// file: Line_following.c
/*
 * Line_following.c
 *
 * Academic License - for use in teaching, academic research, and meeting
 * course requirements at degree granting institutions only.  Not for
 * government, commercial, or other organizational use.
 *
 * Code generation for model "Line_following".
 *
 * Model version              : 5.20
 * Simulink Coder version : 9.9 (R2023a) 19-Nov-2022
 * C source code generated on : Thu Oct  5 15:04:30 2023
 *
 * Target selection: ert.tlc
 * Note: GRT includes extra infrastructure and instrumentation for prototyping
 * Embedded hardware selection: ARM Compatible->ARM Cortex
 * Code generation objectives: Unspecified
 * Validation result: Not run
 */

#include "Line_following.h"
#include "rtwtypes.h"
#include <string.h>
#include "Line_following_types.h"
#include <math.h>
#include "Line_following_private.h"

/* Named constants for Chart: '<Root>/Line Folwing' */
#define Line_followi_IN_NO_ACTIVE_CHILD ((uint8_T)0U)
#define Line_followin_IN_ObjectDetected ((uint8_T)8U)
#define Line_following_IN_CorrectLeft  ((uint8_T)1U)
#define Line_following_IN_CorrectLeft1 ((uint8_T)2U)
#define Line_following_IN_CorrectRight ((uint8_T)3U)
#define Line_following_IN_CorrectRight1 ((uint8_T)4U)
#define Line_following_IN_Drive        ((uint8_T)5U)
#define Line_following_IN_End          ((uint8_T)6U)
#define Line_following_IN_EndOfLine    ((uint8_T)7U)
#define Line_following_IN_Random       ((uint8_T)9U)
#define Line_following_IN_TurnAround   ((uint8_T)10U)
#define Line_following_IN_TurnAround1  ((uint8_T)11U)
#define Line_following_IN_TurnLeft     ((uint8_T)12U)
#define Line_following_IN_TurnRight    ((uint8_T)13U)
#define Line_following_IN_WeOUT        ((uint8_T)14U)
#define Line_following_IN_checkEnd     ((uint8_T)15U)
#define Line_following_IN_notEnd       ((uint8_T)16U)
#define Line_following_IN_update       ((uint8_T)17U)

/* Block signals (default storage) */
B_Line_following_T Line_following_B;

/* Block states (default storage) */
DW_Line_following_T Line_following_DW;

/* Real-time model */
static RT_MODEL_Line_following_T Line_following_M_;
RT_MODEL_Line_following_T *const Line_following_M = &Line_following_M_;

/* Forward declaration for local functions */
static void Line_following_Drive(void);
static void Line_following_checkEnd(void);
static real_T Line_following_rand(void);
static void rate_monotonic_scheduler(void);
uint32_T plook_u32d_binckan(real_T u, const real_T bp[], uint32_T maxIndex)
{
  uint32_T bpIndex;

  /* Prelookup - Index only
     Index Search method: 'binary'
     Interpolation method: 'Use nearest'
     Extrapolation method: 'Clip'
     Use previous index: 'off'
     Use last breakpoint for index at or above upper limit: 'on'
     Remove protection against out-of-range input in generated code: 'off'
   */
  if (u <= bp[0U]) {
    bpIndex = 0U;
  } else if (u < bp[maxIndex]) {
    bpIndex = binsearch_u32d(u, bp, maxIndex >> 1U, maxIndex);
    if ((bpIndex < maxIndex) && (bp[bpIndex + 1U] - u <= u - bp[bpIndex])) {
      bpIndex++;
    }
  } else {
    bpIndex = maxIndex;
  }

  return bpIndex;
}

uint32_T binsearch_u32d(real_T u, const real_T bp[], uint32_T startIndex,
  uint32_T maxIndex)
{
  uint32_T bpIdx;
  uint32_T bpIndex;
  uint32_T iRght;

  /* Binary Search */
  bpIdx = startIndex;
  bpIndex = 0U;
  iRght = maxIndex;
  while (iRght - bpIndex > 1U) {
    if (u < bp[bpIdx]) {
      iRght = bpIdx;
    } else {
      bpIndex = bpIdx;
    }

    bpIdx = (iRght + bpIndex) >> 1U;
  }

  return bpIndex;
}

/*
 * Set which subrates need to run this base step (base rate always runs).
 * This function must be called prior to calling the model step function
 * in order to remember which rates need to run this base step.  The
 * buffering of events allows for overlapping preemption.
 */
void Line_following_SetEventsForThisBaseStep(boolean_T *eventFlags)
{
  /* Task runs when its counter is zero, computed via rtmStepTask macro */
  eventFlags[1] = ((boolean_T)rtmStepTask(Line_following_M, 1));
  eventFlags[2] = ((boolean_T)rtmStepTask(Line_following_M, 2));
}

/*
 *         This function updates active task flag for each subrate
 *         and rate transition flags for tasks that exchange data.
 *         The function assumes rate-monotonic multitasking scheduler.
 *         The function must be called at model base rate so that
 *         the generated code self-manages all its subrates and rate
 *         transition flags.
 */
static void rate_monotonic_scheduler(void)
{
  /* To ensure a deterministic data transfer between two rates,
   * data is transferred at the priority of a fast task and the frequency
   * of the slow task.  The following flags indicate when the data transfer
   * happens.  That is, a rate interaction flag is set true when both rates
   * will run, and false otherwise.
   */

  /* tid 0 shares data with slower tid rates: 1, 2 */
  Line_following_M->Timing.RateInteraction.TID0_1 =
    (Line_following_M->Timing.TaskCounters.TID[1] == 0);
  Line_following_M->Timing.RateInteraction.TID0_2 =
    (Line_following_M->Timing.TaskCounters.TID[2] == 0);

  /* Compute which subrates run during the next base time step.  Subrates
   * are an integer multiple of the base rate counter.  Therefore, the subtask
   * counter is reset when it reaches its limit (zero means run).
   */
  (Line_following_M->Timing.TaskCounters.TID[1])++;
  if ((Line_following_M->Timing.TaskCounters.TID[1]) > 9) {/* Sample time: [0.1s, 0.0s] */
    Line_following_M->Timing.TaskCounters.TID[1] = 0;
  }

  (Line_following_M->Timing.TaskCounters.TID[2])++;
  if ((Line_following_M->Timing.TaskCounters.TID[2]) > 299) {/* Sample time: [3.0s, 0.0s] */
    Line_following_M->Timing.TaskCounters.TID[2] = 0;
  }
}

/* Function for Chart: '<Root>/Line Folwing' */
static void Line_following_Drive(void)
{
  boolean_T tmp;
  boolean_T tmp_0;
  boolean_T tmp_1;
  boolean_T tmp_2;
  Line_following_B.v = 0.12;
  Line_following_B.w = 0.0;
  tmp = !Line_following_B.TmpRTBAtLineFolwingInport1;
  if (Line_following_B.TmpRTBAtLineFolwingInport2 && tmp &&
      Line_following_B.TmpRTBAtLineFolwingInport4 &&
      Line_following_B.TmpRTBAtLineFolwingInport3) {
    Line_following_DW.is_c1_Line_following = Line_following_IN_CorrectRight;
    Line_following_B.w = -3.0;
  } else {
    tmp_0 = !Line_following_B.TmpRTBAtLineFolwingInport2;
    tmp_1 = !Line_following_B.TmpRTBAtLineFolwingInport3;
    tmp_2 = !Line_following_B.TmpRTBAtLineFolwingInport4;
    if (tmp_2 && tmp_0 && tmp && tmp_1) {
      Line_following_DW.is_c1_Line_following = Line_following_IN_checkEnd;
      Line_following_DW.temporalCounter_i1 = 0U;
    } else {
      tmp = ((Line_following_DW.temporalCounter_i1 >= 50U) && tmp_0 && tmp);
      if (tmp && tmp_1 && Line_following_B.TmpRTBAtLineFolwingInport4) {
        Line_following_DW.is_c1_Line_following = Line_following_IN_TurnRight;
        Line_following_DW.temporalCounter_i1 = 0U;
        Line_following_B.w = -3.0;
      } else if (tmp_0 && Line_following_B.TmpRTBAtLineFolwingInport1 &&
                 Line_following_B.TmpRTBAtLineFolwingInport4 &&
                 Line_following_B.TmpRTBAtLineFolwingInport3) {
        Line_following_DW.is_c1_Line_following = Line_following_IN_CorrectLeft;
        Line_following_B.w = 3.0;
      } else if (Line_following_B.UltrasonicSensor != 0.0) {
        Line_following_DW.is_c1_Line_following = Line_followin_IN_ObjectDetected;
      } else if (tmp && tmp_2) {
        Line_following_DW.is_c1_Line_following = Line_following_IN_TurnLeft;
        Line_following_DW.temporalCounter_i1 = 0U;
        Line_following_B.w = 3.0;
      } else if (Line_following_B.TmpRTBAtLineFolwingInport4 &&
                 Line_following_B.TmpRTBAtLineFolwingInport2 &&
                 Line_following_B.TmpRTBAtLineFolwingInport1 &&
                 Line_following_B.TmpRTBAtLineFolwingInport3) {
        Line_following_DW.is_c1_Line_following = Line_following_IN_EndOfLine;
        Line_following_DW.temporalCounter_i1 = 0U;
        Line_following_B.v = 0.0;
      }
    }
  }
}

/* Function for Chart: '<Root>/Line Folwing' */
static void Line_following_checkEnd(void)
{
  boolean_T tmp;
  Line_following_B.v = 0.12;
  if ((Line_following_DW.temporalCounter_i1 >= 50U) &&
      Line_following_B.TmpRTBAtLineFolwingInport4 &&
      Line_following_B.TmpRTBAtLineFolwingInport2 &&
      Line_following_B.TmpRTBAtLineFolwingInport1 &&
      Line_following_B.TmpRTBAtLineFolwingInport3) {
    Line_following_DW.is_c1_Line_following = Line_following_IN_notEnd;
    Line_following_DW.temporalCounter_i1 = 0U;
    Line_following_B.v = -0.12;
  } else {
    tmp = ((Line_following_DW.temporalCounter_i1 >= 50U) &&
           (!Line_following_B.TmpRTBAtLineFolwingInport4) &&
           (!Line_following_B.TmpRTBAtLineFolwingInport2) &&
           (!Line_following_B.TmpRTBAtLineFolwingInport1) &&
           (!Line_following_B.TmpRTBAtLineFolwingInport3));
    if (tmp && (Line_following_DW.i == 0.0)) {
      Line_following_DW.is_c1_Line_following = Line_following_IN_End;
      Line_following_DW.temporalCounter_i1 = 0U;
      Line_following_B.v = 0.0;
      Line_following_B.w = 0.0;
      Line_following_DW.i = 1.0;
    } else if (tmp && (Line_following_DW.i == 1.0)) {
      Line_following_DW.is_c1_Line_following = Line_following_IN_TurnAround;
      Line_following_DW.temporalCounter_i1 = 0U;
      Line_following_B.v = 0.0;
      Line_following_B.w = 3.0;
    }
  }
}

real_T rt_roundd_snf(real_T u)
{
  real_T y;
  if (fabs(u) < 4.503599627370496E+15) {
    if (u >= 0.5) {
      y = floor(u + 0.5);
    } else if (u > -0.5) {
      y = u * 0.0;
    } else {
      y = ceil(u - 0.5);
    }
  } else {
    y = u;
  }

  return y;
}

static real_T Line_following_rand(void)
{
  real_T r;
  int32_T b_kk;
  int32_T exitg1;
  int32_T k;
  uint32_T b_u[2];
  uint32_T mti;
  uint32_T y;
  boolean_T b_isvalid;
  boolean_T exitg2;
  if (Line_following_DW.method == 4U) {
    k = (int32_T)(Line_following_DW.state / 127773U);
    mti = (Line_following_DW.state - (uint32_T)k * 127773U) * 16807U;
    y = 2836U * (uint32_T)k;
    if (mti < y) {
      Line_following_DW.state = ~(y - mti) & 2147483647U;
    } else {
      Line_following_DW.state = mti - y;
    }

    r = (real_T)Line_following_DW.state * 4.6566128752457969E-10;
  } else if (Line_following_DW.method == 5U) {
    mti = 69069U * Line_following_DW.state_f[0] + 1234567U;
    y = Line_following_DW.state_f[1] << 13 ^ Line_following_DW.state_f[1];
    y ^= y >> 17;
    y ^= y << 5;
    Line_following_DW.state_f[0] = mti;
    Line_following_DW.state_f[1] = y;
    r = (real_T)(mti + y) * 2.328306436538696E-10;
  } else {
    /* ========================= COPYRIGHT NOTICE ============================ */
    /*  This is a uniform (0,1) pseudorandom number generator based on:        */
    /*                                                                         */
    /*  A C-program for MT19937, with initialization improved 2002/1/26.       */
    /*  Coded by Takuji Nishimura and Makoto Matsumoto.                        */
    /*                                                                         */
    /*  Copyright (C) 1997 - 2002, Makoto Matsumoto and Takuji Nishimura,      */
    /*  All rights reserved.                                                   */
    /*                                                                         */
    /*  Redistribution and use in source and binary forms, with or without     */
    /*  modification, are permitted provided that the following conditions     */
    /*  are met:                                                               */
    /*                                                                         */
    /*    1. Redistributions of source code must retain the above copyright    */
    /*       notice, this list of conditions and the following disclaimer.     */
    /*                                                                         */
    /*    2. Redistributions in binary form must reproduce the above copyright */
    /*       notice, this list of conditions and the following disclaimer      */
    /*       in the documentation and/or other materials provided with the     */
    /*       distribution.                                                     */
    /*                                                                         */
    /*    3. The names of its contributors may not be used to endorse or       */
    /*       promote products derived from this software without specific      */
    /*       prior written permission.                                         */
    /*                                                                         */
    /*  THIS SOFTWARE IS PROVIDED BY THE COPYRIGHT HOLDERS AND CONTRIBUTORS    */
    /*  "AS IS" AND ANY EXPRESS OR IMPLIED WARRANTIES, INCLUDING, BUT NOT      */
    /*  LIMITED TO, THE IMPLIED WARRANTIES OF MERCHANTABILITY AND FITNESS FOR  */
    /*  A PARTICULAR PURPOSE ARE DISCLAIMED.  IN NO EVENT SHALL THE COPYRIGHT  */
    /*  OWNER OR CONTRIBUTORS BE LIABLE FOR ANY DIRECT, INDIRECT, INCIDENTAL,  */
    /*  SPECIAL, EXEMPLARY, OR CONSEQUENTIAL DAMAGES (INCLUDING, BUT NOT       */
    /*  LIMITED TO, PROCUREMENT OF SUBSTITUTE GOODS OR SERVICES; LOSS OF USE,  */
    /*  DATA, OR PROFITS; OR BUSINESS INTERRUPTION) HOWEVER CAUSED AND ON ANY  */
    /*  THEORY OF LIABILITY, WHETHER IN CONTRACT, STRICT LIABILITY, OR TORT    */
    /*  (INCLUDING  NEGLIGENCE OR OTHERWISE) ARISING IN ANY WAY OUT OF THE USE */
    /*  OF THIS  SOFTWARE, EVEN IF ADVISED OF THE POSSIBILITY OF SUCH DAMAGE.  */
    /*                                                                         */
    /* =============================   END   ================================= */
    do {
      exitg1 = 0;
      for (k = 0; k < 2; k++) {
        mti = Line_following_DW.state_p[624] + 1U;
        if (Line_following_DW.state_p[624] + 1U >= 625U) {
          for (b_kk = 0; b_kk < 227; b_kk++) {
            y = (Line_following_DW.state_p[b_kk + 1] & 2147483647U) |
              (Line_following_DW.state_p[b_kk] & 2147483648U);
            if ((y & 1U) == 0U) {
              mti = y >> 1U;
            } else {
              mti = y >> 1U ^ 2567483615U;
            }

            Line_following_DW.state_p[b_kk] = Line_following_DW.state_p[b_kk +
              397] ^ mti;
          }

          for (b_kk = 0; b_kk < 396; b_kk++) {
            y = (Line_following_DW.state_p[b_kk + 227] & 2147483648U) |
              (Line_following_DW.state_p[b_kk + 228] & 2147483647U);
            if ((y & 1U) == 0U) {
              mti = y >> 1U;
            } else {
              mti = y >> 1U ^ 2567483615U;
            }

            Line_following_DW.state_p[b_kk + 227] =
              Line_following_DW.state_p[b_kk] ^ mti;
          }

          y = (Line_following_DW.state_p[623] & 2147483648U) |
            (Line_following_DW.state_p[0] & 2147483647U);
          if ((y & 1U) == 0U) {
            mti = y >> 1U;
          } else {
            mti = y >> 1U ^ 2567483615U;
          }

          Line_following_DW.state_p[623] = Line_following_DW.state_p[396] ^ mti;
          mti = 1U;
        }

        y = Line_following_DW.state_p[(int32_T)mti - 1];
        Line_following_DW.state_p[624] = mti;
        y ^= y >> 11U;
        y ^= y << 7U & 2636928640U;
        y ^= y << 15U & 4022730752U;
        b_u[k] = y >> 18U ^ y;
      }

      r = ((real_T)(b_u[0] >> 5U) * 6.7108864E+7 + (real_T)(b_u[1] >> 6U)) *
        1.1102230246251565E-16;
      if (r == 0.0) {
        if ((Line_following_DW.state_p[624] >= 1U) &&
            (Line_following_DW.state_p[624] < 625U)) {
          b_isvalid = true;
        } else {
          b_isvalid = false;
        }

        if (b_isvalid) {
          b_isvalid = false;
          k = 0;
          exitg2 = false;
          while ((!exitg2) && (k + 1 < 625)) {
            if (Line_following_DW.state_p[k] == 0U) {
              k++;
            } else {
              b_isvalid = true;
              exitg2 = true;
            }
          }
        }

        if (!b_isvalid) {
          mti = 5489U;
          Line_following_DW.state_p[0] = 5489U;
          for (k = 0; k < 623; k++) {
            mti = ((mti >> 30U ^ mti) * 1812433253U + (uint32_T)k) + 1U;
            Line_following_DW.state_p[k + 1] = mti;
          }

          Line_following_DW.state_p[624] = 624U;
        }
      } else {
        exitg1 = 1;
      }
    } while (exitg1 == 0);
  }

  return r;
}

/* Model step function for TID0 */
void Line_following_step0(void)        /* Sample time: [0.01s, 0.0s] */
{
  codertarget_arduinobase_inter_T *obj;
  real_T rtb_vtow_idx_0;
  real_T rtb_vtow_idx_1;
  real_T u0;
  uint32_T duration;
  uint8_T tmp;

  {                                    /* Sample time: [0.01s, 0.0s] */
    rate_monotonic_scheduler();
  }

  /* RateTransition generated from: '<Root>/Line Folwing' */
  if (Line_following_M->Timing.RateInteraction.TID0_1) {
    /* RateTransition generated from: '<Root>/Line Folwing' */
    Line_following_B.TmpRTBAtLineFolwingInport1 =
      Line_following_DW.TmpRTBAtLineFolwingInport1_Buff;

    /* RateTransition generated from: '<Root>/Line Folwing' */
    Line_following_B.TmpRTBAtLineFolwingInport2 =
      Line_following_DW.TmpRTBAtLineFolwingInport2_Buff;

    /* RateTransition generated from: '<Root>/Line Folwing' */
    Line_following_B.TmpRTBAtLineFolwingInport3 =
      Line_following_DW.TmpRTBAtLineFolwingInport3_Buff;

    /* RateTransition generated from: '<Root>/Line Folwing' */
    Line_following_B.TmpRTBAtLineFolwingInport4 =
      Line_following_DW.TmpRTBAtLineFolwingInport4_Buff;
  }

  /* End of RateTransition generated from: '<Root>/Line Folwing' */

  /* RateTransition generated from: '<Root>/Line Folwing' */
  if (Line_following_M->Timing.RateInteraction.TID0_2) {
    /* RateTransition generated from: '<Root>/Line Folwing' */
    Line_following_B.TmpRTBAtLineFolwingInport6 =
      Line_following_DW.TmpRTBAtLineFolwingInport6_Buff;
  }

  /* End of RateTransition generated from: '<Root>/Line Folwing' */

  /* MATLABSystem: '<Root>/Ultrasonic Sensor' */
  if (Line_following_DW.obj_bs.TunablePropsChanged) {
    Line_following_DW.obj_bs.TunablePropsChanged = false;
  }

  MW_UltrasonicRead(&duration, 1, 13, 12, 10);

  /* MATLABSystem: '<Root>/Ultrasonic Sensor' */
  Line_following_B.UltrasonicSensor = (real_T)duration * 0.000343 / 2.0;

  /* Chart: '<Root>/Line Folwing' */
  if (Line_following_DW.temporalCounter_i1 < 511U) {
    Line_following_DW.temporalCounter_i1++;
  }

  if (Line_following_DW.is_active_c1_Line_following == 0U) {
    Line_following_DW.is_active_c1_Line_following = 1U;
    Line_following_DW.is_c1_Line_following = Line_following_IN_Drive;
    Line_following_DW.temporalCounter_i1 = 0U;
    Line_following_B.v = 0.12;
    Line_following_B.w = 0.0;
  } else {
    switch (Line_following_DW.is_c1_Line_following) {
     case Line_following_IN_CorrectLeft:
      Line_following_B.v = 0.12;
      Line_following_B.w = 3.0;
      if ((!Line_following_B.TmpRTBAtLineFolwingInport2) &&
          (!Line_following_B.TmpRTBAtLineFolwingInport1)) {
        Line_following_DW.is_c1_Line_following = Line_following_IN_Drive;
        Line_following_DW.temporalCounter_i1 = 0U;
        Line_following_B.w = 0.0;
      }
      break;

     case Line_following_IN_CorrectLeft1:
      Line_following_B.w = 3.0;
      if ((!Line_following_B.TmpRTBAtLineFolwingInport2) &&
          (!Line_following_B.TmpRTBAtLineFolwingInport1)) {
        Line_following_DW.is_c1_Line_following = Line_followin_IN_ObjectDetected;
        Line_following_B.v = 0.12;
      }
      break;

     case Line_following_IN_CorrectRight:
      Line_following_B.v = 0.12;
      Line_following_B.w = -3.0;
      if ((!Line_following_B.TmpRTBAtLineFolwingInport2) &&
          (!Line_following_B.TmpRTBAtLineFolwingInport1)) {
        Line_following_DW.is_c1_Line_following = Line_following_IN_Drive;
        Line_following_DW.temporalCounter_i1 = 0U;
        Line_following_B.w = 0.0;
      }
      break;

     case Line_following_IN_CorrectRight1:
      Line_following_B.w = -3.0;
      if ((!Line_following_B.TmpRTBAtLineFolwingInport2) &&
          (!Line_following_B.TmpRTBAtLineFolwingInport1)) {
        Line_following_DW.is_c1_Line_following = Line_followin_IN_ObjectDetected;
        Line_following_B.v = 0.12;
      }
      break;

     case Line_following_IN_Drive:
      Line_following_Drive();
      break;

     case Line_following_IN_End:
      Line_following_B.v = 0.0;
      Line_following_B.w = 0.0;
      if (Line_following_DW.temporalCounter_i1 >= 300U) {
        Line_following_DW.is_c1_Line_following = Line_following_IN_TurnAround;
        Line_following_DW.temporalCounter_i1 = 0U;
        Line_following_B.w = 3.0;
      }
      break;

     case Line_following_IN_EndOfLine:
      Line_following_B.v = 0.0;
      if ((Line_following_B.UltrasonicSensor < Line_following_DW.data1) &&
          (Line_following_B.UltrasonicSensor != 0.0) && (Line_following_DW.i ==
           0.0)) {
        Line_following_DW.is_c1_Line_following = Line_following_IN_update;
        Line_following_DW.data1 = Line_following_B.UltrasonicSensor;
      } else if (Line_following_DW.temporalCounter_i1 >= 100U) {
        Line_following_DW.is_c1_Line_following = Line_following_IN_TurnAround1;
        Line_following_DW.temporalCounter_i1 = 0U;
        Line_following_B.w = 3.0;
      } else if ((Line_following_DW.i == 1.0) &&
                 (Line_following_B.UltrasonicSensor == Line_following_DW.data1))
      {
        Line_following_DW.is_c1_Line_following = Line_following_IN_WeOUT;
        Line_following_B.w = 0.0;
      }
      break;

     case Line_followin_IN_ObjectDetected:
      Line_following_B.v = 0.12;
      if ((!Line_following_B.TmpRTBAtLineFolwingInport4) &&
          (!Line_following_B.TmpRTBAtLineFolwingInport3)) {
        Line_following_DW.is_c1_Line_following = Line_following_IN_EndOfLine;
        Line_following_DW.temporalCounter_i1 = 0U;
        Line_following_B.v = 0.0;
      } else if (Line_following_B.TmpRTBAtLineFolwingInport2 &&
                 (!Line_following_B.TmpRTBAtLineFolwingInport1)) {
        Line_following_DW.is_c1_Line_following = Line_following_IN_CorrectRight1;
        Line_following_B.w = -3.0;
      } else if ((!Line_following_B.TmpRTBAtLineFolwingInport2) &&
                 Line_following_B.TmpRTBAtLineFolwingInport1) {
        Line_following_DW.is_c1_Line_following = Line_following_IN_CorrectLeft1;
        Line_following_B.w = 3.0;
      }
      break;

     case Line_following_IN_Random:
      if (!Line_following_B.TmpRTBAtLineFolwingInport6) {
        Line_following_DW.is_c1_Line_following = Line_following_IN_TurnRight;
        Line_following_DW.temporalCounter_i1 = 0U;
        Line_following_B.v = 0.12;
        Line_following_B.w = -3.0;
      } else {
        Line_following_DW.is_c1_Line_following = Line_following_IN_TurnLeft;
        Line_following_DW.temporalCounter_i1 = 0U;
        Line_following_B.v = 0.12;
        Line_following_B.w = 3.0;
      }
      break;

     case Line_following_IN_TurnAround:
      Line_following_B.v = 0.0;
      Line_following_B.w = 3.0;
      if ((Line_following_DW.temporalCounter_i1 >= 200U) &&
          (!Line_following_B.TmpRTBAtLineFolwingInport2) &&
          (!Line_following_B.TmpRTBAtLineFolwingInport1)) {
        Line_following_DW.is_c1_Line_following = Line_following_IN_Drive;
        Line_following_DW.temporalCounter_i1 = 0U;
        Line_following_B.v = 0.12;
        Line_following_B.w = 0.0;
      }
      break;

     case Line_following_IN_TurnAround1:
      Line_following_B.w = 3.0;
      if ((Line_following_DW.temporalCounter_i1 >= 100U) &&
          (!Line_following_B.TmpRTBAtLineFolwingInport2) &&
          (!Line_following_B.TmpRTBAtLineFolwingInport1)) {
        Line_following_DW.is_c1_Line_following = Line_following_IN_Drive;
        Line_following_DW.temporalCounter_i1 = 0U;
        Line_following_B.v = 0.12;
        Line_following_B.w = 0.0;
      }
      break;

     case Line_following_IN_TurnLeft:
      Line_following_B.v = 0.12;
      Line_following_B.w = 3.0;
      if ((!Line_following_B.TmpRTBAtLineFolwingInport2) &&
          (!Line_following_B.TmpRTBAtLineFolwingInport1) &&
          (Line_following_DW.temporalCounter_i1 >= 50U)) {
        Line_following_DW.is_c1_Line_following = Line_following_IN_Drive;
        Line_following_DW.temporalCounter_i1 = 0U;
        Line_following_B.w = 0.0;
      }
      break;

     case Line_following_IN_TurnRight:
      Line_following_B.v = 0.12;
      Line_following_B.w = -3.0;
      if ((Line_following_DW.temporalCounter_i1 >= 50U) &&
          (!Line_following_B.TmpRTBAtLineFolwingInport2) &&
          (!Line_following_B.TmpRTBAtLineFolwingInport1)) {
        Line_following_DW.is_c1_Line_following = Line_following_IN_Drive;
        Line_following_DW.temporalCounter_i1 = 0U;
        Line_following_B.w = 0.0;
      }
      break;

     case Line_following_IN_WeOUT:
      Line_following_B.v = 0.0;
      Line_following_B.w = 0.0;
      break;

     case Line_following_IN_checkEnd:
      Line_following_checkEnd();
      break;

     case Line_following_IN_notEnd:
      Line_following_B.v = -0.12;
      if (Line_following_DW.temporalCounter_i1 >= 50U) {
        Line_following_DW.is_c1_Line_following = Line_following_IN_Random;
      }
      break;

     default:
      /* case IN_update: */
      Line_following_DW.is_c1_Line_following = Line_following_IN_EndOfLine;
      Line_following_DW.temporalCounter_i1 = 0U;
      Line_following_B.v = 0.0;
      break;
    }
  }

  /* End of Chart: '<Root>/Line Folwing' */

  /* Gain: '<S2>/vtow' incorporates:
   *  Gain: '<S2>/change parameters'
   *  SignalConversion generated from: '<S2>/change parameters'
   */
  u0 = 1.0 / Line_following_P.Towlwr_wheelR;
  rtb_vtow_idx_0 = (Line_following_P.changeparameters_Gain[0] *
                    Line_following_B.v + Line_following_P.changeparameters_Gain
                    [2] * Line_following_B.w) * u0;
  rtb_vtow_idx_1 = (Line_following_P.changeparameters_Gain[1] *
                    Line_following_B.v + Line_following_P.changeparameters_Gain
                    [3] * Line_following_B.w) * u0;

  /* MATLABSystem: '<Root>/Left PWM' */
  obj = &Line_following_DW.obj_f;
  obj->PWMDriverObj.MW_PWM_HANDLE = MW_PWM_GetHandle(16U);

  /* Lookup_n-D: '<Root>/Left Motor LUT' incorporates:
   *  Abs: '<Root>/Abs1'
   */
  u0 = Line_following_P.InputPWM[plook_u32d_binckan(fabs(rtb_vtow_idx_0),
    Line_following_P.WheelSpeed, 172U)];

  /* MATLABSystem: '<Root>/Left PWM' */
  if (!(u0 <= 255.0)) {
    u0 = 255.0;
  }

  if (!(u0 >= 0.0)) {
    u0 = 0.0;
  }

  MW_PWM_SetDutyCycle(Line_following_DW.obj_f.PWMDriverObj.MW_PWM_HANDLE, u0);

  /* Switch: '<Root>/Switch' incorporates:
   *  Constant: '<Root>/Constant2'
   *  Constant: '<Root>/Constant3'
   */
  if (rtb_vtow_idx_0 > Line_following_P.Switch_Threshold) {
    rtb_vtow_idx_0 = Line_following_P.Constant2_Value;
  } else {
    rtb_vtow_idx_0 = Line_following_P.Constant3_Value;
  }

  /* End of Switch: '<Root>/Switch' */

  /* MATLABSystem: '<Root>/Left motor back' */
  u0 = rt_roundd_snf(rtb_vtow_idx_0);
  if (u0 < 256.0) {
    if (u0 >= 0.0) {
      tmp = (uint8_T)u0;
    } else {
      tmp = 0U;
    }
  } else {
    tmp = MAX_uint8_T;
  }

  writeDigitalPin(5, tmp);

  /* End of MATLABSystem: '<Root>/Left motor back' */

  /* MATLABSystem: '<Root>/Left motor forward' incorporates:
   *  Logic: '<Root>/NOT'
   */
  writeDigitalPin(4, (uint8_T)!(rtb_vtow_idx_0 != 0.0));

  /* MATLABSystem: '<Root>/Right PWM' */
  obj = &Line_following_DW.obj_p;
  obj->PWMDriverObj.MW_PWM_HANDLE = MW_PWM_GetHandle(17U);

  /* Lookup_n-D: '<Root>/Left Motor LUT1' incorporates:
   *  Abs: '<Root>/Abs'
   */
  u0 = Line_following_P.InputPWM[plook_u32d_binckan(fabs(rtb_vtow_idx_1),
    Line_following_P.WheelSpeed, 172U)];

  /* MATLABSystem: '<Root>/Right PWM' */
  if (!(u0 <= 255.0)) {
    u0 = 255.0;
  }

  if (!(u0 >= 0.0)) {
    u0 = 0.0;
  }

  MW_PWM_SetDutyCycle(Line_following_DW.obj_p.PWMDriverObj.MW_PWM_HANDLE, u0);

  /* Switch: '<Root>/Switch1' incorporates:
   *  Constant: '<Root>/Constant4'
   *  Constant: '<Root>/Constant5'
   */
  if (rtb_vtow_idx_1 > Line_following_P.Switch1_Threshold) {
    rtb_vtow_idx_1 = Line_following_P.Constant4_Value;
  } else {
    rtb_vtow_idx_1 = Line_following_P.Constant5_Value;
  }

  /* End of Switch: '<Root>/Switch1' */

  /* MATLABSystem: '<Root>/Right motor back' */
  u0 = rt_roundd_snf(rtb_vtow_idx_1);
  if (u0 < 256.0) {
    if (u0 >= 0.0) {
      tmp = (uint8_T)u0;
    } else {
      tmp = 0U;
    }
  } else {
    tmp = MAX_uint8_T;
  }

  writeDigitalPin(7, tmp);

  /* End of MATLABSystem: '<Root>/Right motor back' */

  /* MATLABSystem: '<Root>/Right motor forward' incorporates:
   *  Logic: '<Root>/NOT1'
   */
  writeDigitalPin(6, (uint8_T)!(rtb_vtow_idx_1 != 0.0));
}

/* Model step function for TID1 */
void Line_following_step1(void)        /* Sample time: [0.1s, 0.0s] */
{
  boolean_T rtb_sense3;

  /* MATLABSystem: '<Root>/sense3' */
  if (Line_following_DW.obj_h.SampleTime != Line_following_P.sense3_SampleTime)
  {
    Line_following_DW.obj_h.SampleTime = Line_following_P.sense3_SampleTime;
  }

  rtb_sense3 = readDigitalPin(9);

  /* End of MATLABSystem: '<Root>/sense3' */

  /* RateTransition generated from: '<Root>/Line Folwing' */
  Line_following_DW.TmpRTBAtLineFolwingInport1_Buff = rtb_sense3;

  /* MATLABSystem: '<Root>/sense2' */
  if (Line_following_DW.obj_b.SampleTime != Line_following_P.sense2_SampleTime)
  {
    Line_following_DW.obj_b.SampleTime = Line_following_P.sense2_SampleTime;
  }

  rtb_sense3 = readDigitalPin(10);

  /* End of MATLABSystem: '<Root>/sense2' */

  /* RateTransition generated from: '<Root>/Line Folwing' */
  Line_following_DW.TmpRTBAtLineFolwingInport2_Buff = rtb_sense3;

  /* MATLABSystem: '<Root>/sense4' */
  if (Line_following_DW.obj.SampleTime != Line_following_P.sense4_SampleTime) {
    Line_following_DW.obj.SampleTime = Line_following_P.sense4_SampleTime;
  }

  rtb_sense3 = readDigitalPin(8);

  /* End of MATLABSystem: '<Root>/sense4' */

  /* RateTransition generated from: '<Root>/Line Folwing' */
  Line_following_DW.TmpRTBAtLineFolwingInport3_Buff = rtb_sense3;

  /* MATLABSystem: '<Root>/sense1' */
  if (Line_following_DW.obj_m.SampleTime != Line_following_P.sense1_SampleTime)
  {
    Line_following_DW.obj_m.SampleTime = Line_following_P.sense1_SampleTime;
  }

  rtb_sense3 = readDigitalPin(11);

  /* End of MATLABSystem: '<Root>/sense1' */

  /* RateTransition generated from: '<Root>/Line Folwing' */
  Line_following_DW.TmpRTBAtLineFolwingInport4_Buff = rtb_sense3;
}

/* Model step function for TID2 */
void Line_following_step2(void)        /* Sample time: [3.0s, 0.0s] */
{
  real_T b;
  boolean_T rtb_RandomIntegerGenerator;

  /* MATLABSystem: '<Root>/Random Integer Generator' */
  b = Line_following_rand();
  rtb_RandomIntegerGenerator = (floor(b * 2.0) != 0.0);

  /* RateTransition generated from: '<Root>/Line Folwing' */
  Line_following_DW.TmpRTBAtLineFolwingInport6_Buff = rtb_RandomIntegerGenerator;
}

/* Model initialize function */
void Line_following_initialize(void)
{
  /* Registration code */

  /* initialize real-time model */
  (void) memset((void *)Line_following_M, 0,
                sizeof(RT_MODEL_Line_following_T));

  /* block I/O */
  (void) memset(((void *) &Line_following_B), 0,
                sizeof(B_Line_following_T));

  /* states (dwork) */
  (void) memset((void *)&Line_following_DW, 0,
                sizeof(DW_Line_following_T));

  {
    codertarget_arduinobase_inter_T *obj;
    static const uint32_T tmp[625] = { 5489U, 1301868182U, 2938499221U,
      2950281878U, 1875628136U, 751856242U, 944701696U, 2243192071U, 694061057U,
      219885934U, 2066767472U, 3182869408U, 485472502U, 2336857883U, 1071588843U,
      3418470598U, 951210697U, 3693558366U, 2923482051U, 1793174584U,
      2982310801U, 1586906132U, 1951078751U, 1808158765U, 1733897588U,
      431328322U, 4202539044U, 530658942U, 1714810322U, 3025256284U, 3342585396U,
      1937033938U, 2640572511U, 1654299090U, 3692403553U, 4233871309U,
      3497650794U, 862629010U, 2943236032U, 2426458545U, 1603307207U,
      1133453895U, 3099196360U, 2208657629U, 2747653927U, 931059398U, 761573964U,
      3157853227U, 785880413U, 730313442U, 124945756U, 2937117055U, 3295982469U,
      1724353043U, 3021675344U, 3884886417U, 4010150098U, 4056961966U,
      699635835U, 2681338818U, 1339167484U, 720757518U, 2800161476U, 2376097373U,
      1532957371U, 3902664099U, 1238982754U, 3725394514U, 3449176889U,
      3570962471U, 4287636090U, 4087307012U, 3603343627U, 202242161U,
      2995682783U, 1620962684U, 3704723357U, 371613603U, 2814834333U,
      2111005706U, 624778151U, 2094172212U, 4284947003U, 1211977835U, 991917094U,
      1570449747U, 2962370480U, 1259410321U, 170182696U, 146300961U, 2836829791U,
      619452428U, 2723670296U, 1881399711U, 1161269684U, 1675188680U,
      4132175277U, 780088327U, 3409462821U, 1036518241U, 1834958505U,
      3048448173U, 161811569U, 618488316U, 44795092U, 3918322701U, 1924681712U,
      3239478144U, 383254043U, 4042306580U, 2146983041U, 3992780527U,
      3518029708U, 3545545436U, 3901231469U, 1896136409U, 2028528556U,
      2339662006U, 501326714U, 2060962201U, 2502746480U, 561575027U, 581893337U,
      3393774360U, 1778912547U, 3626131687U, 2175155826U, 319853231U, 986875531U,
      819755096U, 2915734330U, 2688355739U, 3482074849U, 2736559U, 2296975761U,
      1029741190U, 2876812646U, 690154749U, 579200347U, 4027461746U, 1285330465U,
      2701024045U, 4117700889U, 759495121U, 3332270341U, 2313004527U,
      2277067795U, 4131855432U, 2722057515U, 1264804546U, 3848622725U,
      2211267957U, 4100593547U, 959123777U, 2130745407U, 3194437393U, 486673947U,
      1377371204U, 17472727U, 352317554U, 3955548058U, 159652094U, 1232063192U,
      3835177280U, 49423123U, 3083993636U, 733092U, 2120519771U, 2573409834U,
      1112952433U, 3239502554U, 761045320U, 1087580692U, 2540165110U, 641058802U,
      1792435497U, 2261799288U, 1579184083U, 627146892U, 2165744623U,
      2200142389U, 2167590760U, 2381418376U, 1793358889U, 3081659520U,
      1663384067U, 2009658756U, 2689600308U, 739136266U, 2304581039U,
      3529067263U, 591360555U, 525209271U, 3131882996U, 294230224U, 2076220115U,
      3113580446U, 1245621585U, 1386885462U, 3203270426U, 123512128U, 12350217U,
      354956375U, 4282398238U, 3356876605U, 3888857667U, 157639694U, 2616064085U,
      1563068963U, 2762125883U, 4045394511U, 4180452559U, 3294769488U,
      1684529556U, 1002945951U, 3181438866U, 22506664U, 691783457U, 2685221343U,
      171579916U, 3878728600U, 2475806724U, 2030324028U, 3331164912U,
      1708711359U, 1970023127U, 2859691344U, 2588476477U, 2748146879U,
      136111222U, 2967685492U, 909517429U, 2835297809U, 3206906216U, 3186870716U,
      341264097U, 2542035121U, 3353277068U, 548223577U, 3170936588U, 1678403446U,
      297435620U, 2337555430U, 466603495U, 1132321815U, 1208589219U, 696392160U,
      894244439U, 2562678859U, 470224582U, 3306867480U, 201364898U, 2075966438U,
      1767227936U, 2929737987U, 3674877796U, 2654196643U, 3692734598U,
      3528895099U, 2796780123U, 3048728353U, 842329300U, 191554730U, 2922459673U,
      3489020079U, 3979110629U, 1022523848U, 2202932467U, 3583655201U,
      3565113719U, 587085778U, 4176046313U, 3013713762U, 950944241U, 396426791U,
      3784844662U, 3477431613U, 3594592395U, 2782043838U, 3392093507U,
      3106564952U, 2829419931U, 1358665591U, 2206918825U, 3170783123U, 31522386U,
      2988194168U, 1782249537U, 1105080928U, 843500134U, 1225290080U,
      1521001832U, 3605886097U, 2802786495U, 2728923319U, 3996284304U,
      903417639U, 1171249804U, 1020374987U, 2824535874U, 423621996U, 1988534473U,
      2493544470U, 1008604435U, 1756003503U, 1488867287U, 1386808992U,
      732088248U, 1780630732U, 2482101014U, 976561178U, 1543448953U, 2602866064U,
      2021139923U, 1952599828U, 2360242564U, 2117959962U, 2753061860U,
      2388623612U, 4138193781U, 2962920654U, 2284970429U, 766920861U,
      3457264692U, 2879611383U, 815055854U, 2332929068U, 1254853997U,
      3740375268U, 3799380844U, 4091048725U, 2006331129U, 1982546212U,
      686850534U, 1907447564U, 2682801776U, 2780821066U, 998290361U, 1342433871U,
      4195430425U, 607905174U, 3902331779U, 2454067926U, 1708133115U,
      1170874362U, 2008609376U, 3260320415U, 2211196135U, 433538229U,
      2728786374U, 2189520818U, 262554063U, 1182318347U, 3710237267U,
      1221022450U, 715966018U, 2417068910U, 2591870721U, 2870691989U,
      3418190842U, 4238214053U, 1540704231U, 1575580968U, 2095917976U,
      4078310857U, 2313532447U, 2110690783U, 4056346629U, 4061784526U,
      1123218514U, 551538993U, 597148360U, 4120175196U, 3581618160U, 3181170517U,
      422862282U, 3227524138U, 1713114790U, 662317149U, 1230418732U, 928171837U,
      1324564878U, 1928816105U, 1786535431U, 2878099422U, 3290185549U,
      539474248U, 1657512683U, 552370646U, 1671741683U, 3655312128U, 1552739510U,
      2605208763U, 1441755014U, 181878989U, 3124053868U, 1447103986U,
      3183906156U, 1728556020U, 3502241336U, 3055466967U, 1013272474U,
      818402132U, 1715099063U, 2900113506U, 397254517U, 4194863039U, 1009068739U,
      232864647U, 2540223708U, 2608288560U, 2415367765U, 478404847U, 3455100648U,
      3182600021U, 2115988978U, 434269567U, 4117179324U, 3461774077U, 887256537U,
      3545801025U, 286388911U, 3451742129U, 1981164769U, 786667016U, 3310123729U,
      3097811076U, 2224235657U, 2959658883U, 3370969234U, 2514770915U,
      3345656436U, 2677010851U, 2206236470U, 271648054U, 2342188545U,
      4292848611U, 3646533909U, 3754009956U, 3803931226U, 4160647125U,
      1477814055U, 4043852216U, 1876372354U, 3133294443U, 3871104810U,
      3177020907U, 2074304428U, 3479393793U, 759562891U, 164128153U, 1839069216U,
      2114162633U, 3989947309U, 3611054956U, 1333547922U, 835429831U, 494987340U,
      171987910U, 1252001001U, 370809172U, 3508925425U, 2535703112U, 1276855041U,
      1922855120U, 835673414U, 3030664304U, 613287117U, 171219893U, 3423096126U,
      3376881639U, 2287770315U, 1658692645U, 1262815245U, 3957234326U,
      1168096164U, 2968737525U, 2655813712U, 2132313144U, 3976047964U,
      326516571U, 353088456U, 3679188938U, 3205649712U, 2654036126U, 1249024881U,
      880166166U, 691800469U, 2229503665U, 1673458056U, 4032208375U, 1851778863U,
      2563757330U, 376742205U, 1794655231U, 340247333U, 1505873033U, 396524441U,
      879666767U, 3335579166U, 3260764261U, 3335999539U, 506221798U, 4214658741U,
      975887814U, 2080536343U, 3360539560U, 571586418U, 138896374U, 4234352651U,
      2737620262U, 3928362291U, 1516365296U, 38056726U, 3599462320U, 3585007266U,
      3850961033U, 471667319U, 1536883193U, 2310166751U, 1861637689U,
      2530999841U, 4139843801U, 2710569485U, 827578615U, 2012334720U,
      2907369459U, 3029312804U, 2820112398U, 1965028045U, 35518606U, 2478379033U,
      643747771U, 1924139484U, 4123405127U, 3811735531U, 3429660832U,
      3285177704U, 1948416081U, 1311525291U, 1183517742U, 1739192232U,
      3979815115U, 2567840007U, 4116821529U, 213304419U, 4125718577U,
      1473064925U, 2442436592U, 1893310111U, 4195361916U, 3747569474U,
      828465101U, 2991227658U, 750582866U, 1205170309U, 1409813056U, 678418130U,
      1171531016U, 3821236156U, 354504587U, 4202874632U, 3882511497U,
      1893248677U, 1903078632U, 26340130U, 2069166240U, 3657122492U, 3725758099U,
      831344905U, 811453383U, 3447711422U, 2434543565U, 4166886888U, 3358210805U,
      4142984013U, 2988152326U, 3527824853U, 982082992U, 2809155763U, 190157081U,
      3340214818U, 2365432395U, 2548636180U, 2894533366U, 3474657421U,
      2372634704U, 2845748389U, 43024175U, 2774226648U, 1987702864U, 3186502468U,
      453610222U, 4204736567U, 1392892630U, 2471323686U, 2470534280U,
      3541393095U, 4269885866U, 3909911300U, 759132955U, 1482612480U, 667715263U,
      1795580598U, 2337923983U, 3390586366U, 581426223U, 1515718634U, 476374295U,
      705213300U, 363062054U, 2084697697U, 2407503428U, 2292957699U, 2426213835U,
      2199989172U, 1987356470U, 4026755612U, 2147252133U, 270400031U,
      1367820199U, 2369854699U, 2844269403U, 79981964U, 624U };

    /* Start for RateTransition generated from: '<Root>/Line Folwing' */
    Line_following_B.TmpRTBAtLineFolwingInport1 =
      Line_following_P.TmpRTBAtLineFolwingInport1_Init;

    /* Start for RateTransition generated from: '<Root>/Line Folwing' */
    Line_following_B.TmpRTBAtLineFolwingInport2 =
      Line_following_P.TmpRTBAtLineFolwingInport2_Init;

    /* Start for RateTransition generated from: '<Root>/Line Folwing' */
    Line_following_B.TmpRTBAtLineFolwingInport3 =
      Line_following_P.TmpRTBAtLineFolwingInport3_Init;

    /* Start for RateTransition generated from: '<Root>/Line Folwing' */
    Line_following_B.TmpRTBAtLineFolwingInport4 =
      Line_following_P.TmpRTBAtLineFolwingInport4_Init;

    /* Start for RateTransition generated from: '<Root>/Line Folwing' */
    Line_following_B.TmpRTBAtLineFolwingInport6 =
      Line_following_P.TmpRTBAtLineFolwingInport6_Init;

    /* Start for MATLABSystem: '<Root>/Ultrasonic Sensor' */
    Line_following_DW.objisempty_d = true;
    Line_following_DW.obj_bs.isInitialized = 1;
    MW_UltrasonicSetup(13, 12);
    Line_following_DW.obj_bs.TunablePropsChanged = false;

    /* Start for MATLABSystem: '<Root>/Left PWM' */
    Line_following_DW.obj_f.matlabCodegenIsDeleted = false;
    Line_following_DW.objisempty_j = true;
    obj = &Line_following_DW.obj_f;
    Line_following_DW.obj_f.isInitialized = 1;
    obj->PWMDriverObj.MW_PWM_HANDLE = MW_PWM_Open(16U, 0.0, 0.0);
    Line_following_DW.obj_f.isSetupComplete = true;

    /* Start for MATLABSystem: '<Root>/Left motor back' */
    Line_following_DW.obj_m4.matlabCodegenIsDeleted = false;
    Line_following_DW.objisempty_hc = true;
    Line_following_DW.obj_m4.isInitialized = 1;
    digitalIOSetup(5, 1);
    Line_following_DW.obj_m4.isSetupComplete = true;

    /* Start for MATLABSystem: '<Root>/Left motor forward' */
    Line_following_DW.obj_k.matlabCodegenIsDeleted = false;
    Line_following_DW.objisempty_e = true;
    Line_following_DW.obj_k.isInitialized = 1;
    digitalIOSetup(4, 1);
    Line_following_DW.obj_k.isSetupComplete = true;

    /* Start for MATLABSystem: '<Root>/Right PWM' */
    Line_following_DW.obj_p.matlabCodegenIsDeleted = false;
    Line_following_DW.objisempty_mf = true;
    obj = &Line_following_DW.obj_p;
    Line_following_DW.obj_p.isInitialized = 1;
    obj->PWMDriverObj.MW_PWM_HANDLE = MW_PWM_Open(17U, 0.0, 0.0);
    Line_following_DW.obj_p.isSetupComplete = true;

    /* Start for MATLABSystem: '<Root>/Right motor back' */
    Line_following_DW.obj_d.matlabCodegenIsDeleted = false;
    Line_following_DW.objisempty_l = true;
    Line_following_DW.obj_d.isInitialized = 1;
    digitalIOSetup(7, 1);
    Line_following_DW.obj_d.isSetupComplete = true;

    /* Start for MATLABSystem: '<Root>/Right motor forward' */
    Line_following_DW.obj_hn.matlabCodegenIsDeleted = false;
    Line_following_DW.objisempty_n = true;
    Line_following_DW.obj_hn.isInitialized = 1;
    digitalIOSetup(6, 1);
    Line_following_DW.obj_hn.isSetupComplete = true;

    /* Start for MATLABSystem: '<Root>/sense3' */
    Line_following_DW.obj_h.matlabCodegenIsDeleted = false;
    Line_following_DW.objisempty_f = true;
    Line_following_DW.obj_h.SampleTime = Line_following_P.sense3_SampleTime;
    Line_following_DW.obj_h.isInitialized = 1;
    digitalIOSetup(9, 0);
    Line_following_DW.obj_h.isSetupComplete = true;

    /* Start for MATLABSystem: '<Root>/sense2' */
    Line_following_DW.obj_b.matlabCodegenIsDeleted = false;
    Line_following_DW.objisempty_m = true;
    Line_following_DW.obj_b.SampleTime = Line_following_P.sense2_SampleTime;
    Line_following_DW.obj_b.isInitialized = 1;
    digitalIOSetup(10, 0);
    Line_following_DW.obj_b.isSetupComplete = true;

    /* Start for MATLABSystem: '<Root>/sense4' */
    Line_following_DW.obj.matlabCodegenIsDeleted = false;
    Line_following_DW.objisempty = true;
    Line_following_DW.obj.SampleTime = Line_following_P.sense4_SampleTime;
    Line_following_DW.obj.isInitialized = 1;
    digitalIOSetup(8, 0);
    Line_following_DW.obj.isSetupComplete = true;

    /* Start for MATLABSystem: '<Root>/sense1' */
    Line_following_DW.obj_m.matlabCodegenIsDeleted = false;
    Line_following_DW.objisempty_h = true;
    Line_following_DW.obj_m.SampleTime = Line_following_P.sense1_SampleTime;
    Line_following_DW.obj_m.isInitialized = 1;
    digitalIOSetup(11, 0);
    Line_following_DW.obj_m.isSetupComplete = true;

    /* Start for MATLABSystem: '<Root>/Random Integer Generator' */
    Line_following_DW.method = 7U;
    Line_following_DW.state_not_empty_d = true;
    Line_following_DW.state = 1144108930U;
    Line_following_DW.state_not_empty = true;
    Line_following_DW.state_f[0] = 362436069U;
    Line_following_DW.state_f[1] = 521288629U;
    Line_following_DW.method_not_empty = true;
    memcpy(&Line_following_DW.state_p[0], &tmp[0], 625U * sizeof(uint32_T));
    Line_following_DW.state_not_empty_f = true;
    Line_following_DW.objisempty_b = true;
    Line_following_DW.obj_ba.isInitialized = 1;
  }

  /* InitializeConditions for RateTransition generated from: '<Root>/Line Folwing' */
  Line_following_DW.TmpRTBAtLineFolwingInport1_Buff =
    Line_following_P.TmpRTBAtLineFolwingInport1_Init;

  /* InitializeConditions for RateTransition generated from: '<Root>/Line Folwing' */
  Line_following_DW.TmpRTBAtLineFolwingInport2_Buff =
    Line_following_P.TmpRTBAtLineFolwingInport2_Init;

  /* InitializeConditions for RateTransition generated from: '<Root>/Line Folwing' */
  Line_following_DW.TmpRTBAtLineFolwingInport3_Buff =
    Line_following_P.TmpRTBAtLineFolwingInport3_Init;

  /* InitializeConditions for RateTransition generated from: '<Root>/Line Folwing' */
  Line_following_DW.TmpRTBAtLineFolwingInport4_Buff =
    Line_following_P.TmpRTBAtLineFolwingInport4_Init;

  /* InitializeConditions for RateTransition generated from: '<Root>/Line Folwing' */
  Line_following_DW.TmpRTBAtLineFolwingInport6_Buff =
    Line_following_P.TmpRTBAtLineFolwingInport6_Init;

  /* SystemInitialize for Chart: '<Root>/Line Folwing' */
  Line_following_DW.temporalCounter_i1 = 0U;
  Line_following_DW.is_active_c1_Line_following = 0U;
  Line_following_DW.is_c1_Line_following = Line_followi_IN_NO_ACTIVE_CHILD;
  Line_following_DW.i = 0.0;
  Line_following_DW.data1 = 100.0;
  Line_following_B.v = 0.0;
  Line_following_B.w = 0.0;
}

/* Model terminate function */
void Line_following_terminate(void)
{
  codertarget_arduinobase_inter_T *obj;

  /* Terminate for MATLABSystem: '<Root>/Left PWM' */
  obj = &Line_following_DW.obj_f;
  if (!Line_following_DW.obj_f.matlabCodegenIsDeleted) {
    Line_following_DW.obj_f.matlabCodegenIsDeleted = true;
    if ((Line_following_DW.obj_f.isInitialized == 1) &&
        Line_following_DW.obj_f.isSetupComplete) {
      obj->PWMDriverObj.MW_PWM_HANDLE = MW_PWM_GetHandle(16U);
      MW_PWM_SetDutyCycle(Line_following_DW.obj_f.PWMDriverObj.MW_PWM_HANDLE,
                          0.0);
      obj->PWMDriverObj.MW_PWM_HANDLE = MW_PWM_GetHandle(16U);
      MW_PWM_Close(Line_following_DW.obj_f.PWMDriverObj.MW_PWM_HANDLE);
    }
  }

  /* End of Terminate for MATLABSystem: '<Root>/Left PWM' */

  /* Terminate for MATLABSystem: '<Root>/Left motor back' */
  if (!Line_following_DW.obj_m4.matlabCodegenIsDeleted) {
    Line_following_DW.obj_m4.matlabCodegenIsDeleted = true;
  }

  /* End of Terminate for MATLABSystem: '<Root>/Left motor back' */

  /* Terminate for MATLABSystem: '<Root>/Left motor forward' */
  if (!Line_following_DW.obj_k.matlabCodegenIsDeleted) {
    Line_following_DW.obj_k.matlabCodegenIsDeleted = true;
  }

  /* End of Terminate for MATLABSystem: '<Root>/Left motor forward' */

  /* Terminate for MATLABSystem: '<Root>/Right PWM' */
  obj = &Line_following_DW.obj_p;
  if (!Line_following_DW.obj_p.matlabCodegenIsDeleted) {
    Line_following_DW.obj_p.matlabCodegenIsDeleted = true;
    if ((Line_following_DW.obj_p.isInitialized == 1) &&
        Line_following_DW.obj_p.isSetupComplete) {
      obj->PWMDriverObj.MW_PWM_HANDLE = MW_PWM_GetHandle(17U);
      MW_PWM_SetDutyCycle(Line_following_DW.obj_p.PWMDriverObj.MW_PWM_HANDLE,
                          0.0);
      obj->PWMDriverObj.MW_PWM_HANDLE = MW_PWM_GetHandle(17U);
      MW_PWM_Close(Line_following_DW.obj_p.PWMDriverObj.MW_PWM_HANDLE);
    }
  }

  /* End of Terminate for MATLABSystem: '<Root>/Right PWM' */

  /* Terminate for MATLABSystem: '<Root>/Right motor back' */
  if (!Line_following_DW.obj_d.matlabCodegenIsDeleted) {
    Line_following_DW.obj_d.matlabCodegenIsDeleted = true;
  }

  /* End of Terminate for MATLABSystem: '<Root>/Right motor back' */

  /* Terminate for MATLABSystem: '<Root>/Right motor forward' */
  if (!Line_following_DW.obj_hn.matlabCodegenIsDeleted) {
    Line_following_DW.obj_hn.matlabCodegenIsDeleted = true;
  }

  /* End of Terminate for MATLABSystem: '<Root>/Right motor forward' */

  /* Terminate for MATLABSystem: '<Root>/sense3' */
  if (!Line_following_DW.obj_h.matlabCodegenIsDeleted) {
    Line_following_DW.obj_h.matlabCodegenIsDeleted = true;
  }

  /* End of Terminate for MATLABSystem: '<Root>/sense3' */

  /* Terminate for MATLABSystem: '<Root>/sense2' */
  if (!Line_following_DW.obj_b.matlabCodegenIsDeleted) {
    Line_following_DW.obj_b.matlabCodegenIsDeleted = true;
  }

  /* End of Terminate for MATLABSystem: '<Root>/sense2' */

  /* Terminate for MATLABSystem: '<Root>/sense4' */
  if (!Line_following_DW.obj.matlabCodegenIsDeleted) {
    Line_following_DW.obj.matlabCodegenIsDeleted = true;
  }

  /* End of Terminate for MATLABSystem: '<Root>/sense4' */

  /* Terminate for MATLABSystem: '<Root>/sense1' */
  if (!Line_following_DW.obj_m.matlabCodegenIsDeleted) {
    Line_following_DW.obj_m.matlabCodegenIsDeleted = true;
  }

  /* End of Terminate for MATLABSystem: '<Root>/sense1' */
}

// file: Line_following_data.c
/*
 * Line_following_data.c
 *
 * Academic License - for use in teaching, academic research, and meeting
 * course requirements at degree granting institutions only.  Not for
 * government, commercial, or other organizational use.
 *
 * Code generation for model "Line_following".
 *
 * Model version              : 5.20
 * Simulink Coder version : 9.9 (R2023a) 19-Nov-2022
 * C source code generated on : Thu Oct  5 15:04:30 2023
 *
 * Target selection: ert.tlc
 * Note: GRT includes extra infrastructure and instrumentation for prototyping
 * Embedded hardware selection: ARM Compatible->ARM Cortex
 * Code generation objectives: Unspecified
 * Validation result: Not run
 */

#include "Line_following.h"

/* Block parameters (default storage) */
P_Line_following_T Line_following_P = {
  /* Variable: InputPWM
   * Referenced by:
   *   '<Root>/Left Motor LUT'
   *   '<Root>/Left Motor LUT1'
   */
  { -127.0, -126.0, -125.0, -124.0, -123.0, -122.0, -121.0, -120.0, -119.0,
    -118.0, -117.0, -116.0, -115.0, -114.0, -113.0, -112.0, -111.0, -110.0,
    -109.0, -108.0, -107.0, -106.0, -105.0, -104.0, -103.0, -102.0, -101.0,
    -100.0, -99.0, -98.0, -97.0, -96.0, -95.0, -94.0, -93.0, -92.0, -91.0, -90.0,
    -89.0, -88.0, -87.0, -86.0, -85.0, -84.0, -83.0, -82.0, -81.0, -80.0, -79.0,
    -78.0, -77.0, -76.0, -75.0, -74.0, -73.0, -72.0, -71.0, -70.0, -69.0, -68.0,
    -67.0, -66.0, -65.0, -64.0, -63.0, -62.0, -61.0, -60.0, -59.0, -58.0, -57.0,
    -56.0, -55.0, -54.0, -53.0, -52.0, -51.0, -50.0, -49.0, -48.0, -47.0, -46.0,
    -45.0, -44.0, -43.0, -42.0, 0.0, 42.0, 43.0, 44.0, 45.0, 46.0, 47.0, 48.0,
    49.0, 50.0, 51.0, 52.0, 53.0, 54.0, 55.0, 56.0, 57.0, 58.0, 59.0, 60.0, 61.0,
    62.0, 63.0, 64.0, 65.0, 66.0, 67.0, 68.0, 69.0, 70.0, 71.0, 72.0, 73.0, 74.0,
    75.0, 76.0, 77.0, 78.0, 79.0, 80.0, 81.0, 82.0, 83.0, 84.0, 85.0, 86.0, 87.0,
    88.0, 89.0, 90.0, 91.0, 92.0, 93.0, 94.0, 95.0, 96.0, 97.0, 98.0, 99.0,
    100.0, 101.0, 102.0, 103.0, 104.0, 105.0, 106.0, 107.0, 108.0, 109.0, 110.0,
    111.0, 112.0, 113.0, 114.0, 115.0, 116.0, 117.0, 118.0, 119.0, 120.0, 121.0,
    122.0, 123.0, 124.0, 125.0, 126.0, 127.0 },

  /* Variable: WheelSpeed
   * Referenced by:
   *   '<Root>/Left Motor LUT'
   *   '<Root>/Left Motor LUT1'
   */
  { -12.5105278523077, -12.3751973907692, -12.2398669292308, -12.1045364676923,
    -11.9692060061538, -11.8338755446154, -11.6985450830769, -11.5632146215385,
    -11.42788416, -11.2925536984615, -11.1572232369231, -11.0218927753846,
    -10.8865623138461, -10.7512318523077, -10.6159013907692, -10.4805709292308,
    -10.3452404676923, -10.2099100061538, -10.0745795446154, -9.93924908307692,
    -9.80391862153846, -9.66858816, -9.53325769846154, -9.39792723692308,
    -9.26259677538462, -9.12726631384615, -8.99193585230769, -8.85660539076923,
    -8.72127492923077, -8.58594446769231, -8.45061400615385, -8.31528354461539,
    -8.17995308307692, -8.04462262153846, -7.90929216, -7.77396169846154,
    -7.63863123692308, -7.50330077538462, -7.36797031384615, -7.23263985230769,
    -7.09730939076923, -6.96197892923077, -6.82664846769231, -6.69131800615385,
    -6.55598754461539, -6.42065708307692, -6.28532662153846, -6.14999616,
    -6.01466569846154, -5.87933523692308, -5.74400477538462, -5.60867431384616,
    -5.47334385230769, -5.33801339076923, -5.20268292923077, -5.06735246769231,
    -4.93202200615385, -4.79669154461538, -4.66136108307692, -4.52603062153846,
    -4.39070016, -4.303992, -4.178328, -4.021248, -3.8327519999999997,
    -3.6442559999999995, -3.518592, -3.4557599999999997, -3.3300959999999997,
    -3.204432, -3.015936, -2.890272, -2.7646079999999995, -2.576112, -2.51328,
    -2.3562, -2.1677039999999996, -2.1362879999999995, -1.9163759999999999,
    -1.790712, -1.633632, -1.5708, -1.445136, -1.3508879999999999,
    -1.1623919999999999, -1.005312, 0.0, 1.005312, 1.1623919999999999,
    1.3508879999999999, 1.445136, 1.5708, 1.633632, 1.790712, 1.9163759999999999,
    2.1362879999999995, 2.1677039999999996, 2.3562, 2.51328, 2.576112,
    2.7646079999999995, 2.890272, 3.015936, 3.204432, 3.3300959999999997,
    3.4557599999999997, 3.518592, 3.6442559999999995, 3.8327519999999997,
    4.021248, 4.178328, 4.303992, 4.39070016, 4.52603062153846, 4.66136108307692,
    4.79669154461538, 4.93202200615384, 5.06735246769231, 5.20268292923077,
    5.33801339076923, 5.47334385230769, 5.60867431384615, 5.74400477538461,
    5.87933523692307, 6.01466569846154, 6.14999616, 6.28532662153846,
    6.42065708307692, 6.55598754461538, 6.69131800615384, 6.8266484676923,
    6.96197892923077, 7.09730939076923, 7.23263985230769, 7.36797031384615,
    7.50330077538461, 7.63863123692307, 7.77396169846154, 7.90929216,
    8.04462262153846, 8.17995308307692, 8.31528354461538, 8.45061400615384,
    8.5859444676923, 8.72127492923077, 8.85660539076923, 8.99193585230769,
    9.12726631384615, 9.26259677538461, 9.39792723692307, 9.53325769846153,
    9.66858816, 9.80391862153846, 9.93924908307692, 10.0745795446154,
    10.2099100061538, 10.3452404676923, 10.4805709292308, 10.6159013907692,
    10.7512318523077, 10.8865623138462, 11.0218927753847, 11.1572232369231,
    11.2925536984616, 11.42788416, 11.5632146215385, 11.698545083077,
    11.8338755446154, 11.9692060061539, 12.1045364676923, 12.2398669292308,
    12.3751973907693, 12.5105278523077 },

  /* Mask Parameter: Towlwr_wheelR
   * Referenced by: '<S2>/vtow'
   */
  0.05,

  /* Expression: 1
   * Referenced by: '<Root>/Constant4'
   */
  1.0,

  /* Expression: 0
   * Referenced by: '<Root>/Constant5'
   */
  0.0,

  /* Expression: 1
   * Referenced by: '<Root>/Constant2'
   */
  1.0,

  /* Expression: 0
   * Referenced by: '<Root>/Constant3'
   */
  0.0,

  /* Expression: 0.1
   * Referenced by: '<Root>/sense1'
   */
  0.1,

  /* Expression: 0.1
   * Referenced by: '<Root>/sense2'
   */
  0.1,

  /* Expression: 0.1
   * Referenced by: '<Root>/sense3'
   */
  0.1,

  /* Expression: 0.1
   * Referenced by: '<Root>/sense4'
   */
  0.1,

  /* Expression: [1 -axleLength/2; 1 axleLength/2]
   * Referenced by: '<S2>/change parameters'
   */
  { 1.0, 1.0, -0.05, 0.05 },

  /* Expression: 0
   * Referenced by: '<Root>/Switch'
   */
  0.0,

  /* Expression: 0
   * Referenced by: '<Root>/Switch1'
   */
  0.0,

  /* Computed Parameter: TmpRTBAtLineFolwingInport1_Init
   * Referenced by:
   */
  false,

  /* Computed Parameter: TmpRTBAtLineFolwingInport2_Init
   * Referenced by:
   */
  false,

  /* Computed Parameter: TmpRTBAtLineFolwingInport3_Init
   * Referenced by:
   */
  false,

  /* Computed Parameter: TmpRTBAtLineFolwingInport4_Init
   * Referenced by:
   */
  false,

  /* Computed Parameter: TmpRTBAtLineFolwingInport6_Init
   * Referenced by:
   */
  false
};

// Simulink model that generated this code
simulink model "Line_following"  (R2023a)
settings: Solver=FixedStepDiscrete  StartTime=0.0  StopTime=100  FixedStep=0.01  RelTol=1e-3  EnableMultiTasking=on
undefined symbols (not defined in the file): InputPWM, WheelSpeed
libraries: arduinolib x10, commrandsrc3 x1, mobileRoboticsTrainingLib x1, arduinosensorlib x1

== system Line_following ==
  Abs : Abs  SaturateOnIntegerOverflow=off
  Abs1 : Abs  SaturateOnIntegerOverflow=off
  Constant2 : Constant
  Constant3 : Constant  Value=0
  Constant4 : Constant
  Constant5 : Constant  Value=0
  Display{,1..3} (4 alike) : Display
  Left Motor LUT : Lookup_n-D  NumberOfTableDimensions=1  BreakpointsForDimension1=WheelSpeed  Table=InputPWM  InterpMethod=Nearest  ExtrapMethod=Clip  InternalRulePriority=Speed  RndMeth=Simplest
  Left Motor LUT1 : Lookup_n-D  NumberOfTableDimensions=1  BreakpointsForDimension1=WheelSpeed  Table=InputPWM  InterpMethod=Nearest  ExtrapMethod=Clip  InternalRulePriority=Speed  RndMeth=Simplest
  Left PWM : arduinolib/PWM  pinNumber=16  frequencyType=Default  desiredFrequency=490.2  achievableFrequency=490.2
  Left motor back : arduinolib/Digital Output  pinNumber=5  Direction=output  blockPlatform=arduino
  Left motor forward : arduinolib/Digital Output  pinNumber=4  Direction=output  blockPlatform=arduino
  Line Folwing : Stateflow chart  TreatAsAtomicUnit=on
  NOT : Logic  Operator=NOT  IconShape=distinctive  AllPortsSameDT=off  OutDataTypeStr=boolean
  NOT1 : Logic  Operator=NOT  IconShape=distinctive  AllPortsSameDT=off  OutDataTypeStr=boolean
  Random Integer Generator : commrandsrc3/Random Integer Generator  SetSize=2  SeedSource=Auto  Seed=0  SampleTime=3  SamplesPerFrame=1  OutputDataType=boolean  SimulateUsing=Interpreted execution
  Right PWM : arduinolib/PWM  pinNumber=17  frequencyType=Default  desiredFrequency=490.2  achievableFrequency=490.2
  Right motor back : arduinolib/Digital Output  pinNumber=7  Direction=output  blockPlatform=arduino
  Right motor forward : arduinolib/Digital Output  pinNumber=6  Direction=output  blockPlatform=arduino
  Switch : Switch  Criteria=u2 > Threshold  SaturateOnIntegerOverflow=off  InputSameDT=off
  Switch1 : Switch  Criteria=u2 > Threshold  SaturateOnIntegerOverflow=off  InputSameDT=off
  To wlwr : mobileRoboticsTrainingLib/To wlwr  axleLength=0.1  wheelR=0.05
      link override change parameters: Gain=[1 -axleLength/2; 1 axleLength/2]
  Ultrasonic Sensor : arduinosensorlib/Ultrasonic Sensor  NumSignalPins=2  TrigPin=13  EchoPin=12  SignalPin=3  SampleTime_=0.01  blockPlatform=ARDUINO
  sense1 : arduinolib/Digital Input  pinNumber=11  mode=Default  Direction=input  SampleTime=0.1  blockPlatform=arduino
  sense2 : arduinolib/Digital Input  pinNumber=10  mode=Default  Direction=input  SampleTime=0.1  blockPlatform=arduino
  sense3 : arduinolib/Digital Input  pinNumber=9  mode=Default  Direction=input  SampleTime=0.1  blockPlatform=arduino
  sense4 : arduinolib/Digital Input  pinNumber=8  mode=Default  Direction=input  SampleTime=0.1  blockPlatform=arduino
  wires:
  Line Folwing/2(w) -> To wlwr/2
  Line Folwing/1(v) -> To wlwr/1
  Random Integer Generator/1 -> Line Folwing/6(dir)
  sense1/1 -> Display/1, Line Folwing/4(sense1)
  sense2/1 -> Display1/1, Line Folwing/2(sense2)
  sense3/1 -> Display2/1, Line Folwing/1(sense3)
  sense4/1 -> Display3/1, Line Folwing/3(sense4)
  Ultrasonic Sensor/1 -> Line Folwing/5(ultraSonic)
  Constant3/1 -> Switch/3
  Constant2/1 -> Switch/1
  Switch/1 -> NOT/1, Left motor back/1
  NOT1/1 -> Right motor forward/1
  Abs/1 -> Left Motor LUT1/1  "Left PWM"
  Switch1/1 -> NOT1/1, Right motor back/1
  Constant5/1 -> Switch1/3
  Constant4/1 -> Switch1/1
  Abs1/1 -> Left Motor LUT/1  "Left PWM"
  Left Motor LUT1/1 -> Right PWM/1  "Left PWM"
  To wlwr/2 -> Abs/1, Switch1/2
  Left Motor LUT/1 -> Left PWM/1  "Left PWM"
  To wlwr/1 -> Abs1/1, Switch/2
  NOT/1 -> Left motor forward/1

== stateflow chart Line_following/Line Folwing ==
  state Random
    entry:
    dir;
  state notEnd
    entry:
    v=-0.5;
  state End
    entry:
    v=0;
    w=0;
    i=1;
  state TurnAround
    entry:
    v=0;
    w=1;
  state checkEnd
    entry:
    v=0.5;
  state TurnLeft
    entry:
    v=0.5;
    w=1;
  state TurnRight
    entry:
    v=0.5;
    w=-1;
  state Drive
    entry:
    v=0.5;
    w=0;
    i;
    n;
    data1;
  state CorrectLeft
    entry:
    v=0.5;
    w=1
  state CorrectRight
    entry:
    v=0.5;
    w=-1
  state ObjectDetected
    entry:
    v=0.5;
  state CorrectRight1
    entry:
    w=-1;
  state CorrectLeft1
    entry:
    w=1;
  state TurnAround1
    entry:
    w=1;
  state EndOfLine
    entry:
    v=0;
  state update
    entry:
    data1=ultraSonic;
  state WeOUT
    entry:
    v=0;
    w=0;
  checkEnd -> TurnAround [order 3] : [after(0.5,sec) &&sense1 ==0 && sense2 == 0 && sense3 ==0 && sense4==0 && i==1]
  Random -> TurnLeft [order 2] : [dir==1]
  Random -> TurnRight [order 1] : [dir==0]
  notEnd -> Random : [after(0.5,sec)]
  checkEnd -> notEnd [order 1] : [after(0.5,sec) &&sense1 == 1 && sense2 == 1 && sense3 ==1 && sense4==1 ]
  End -> TurnAround : [after(3,sec)]
  checkEnd -> End [order 2] : [after(0.5,sec) &&sense1 ==0 && sense2 == 0 && sense3 ==0 && sense4==0 && i==0]
  TurnAround -> Drive : [after(2,sec) && sense2 == 0 && sense3 == 0]
  Drive -> checkEnd [order 2] : [sense1 == 0 && sense2 == 0 && sense3 == 0 && sense4==0]
  (default) -> Drive
  TurnRight -> Drive : [after(0.5,sec) && sense2 ==0 && sense3 ==0]
  Drive -> TurnLeft [order 6] : [after(0.5,sec) && sense2 == 0 && sense3 == 0 && sense1 == 0 ]
  TurnLeft -> Drive : [sense2==0 && sense3==0 && after(0.5,sec)]
  Drive -> TurnRight [order 3] : [after(0.5,sec) && sense2 == 0 && sense3 == 0 && sense4 == 0 && sense1==1]
  Drive -> CorrectLeft [order 4] : [sense2==0 && sense3 ==1 && sense1 == 1 &&sense4 ==1]
  Drive -> CorrectRight [order 1] : [sense2==1 && sense3 ==0 && sense1 == 1 &&sense4 ==1]
  CorrectLeft -> Drive : [sense2 ==0 && sense3 ==0]
  CorrectRight -> Drive : [sense2==0 && sense3 == 0]
  TurnAround1 -> Drive : [after(1,sec) && sense2 == 0 && sense3 == 0]
  Drive -> EndOfLine [order 7] : [sense1 == 1 && sense2 == 1 && sense3 == 1 && sense4==1]
  Drive -> ObjectDetected [order 5] : [ultraSonic ~= 0]
  ObjectDetected -> CorrectRight1 [order 2] : [sense2==1 && sense3 ==0]
  ObjectDetected -> CorrectLeft1 [order 3] : [sense2==0 && sense3 ==1]
  CorrectRight1 -> ObjectDetected : [sense2==0 && sense3 == 0]
  CorrectLeft1 -> ObjectDetected : [sense2 ==0 && sense3 ==0]
  ObjectDetected -> EndOfLine [order 1] : [sense1 == 0 && sense4 == 0]
  EndOfLine -> TurnAround1 [order 2] : [after(1,sec)]
  update -> EndOfLine
  EndOfLine -> update [order 1] : [ultraSonic<data1 && ultraSonic~=0 && i==0]
  EndOfLine -> WeOUT [order 3] : [i==1 && ultraSonic==data1]
  data: v output; w output; sense3 input; sense2 input; sense4 input; sense1 input; ultraSonic input; i local =0; dir input; n local =1; data1 local =100
